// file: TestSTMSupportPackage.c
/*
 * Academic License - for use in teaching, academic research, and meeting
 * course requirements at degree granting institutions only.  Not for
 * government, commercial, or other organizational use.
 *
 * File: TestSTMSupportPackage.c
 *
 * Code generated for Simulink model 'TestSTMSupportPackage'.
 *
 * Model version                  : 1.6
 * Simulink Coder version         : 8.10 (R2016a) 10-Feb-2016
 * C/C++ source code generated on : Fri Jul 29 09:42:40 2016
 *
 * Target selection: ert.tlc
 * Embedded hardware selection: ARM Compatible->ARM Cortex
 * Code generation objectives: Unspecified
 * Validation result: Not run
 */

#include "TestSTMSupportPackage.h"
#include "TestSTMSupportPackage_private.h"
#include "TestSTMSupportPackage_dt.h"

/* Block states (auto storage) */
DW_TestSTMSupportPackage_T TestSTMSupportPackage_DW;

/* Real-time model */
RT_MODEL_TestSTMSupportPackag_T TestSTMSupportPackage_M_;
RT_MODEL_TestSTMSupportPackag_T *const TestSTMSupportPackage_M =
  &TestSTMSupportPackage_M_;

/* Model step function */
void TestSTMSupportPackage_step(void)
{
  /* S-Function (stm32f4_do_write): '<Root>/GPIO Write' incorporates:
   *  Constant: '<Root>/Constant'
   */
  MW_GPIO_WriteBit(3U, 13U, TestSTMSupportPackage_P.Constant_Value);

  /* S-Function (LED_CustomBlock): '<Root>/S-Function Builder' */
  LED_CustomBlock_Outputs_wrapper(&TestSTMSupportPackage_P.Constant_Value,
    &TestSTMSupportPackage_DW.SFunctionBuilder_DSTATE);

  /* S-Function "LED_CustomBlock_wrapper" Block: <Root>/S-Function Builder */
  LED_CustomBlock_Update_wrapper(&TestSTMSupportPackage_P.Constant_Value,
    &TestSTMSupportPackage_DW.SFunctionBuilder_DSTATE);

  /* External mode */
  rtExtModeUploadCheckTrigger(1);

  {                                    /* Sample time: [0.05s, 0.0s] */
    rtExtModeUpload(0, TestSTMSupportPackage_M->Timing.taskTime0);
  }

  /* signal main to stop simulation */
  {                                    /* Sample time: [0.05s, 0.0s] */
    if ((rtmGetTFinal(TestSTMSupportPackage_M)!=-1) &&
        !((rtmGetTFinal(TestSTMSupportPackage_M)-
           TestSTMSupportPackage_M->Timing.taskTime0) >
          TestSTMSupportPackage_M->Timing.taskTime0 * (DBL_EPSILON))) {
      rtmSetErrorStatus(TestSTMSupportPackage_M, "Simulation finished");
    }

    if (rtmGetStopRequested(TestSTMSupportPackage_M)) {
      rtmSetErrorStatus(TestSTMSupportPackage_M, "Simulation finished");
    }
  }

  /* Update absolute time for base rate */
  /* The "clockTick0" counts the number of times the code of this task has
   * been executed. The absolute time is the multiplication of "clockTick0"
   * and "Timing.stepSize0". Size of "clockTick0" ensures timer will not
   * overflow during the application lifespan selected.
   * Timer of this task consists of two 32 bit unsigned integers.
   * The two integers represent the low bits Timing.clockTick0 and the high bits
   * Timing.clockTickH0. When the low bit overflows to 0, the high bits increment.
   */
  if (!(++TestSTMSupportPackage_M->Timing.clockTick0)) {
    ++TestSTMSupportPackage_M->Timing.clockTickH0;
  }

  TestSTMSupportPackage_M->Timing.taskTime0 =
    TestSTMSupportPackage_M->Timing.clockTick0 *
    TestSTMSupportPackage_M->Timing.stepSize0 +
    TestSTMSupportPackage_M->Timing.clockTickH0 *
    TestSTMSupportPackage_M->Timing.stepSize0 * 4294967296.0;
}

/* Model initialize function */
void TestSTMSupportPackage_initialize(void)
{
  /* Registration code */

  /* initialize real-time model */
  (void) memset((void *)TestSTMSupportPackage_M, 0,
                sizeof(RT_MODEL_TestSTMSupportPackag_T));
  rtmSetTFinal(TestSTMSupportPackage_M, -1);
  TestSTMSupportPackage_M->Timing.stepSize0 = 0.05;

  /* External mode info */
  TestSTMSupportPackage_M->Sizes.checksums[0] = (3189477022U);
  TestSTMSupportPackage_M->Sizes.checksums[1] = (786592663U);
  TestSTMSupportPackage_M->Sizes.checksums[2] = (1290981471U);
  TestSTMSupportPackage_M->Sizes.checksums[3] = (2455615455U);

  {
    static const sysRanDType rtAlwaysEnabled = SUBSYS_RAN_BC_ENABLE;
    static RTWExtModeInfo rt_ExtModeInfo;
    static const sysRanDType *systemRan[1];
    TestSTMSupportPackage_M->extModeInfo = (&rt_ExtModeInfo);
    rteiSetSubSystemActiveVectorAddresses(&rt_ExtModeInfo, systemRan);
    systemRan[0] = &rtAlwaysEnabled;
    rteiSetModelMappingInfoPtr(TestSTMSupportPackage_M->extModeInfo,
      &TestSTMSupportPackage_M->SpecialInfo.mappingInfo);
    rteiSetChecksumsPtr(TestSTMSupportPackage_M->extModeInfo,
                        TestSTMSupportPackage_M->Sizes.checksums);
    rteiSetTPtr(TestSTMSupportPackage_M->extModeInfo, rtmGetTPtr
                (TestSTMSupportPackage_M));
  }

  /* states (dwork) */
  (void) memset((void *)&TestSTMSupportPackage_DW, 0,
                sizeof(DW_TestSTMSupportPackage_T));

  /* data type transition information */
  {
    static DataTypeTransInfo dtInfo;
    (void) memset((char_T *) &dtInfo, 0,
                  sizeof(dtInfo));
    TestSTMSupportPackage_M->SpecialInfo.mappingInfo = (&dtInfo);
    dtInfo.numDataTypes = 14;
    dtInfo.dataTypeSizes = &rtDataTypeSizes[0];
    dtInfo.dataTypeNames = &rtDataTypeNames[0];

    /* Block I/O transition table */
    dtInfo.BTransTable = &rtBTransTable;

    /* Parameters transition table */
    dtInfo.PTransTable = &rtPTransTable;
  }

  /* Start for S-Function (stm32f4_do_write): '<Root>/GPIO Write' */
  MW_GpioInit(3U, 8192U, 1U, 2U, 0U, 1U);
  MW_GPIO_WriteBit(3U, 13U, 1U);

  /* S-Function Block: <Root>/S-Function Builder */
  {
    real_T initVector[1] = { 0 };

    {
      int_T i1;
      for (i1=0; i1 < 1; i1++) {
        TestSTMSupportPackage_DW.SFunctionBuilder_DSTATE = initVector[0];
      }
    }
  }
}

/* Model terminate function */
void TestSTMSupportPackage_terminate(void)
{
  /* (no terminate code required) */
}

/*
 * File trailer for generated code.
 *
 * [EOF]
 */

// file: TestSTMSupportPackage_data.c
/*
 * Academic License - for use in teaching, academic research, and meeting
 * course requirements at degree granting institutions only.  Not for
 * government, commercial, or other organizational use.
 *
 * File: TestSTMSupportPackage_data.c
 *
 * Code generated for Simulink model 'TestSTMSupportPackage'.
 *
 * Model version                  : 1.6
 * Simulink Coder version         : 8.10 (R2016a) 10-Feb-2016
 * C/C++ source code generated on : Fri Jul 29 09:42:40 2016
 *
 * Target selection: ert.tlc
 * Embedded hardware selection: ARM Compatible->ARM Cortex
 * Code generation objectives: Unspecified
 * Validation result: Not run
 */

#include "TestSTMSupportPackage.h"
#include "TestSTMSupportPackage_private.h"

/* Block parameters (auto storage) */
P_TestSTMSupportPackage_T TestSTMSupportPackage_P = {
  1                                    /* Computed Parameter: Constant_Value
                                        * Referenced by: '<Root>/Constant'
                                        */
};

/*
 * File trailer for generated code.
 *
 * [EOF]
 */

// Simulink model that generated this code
simulink model "TestSTMSupportPackage"  (R2016a)
settings: Solver=FixedStepAuto  StartTime=0.0  StopTime=inf  FixedStep=0.05  RelTol=1e-3
libraries: stm32f4lib x1

== system TestSTMSupportPackage ==
  Constant : Constant  OutDataTypeStr=Inherit: Inherit via back propagation
  GPIO Write : stm32f4lib/GPIO Write  gpio_name=GPIOD  pin_number=13  pupd_reg=1  otype_reg=0  ospeed_reg=2  gpio_init_out=on  toggle_pin=off
  S-Function Builder : S-Function  InitFcn=try, set_param(gcb,'FunctionName','LED_CustomBlock'), end  FunctionName=LED_CustomBlock  SFunctionModules=LED_CustomBlock_wrapper  SFunctionDeploymentMode=off  EnableBusSupport=off  mask(S-Function Builder){}
      mask help: Simulink:masks:SFunctionBuilder_MD
      mask init:
      | val = [[.9  0.75 0.75 1 1 .9 .9 1]',[1 1 0.75 0.75 .9 .9 1 .9]'];try , sys = get_param(gcb,'SfunBuilderFcnName');if isempty(sys), sys = get_param(gcb,'FunctionName'); end,catch, sys = get_param(gcb,'FunctionName'); end
  wires:
  Constant/1 -> S-Function Builder/1, GPIO Write/1
